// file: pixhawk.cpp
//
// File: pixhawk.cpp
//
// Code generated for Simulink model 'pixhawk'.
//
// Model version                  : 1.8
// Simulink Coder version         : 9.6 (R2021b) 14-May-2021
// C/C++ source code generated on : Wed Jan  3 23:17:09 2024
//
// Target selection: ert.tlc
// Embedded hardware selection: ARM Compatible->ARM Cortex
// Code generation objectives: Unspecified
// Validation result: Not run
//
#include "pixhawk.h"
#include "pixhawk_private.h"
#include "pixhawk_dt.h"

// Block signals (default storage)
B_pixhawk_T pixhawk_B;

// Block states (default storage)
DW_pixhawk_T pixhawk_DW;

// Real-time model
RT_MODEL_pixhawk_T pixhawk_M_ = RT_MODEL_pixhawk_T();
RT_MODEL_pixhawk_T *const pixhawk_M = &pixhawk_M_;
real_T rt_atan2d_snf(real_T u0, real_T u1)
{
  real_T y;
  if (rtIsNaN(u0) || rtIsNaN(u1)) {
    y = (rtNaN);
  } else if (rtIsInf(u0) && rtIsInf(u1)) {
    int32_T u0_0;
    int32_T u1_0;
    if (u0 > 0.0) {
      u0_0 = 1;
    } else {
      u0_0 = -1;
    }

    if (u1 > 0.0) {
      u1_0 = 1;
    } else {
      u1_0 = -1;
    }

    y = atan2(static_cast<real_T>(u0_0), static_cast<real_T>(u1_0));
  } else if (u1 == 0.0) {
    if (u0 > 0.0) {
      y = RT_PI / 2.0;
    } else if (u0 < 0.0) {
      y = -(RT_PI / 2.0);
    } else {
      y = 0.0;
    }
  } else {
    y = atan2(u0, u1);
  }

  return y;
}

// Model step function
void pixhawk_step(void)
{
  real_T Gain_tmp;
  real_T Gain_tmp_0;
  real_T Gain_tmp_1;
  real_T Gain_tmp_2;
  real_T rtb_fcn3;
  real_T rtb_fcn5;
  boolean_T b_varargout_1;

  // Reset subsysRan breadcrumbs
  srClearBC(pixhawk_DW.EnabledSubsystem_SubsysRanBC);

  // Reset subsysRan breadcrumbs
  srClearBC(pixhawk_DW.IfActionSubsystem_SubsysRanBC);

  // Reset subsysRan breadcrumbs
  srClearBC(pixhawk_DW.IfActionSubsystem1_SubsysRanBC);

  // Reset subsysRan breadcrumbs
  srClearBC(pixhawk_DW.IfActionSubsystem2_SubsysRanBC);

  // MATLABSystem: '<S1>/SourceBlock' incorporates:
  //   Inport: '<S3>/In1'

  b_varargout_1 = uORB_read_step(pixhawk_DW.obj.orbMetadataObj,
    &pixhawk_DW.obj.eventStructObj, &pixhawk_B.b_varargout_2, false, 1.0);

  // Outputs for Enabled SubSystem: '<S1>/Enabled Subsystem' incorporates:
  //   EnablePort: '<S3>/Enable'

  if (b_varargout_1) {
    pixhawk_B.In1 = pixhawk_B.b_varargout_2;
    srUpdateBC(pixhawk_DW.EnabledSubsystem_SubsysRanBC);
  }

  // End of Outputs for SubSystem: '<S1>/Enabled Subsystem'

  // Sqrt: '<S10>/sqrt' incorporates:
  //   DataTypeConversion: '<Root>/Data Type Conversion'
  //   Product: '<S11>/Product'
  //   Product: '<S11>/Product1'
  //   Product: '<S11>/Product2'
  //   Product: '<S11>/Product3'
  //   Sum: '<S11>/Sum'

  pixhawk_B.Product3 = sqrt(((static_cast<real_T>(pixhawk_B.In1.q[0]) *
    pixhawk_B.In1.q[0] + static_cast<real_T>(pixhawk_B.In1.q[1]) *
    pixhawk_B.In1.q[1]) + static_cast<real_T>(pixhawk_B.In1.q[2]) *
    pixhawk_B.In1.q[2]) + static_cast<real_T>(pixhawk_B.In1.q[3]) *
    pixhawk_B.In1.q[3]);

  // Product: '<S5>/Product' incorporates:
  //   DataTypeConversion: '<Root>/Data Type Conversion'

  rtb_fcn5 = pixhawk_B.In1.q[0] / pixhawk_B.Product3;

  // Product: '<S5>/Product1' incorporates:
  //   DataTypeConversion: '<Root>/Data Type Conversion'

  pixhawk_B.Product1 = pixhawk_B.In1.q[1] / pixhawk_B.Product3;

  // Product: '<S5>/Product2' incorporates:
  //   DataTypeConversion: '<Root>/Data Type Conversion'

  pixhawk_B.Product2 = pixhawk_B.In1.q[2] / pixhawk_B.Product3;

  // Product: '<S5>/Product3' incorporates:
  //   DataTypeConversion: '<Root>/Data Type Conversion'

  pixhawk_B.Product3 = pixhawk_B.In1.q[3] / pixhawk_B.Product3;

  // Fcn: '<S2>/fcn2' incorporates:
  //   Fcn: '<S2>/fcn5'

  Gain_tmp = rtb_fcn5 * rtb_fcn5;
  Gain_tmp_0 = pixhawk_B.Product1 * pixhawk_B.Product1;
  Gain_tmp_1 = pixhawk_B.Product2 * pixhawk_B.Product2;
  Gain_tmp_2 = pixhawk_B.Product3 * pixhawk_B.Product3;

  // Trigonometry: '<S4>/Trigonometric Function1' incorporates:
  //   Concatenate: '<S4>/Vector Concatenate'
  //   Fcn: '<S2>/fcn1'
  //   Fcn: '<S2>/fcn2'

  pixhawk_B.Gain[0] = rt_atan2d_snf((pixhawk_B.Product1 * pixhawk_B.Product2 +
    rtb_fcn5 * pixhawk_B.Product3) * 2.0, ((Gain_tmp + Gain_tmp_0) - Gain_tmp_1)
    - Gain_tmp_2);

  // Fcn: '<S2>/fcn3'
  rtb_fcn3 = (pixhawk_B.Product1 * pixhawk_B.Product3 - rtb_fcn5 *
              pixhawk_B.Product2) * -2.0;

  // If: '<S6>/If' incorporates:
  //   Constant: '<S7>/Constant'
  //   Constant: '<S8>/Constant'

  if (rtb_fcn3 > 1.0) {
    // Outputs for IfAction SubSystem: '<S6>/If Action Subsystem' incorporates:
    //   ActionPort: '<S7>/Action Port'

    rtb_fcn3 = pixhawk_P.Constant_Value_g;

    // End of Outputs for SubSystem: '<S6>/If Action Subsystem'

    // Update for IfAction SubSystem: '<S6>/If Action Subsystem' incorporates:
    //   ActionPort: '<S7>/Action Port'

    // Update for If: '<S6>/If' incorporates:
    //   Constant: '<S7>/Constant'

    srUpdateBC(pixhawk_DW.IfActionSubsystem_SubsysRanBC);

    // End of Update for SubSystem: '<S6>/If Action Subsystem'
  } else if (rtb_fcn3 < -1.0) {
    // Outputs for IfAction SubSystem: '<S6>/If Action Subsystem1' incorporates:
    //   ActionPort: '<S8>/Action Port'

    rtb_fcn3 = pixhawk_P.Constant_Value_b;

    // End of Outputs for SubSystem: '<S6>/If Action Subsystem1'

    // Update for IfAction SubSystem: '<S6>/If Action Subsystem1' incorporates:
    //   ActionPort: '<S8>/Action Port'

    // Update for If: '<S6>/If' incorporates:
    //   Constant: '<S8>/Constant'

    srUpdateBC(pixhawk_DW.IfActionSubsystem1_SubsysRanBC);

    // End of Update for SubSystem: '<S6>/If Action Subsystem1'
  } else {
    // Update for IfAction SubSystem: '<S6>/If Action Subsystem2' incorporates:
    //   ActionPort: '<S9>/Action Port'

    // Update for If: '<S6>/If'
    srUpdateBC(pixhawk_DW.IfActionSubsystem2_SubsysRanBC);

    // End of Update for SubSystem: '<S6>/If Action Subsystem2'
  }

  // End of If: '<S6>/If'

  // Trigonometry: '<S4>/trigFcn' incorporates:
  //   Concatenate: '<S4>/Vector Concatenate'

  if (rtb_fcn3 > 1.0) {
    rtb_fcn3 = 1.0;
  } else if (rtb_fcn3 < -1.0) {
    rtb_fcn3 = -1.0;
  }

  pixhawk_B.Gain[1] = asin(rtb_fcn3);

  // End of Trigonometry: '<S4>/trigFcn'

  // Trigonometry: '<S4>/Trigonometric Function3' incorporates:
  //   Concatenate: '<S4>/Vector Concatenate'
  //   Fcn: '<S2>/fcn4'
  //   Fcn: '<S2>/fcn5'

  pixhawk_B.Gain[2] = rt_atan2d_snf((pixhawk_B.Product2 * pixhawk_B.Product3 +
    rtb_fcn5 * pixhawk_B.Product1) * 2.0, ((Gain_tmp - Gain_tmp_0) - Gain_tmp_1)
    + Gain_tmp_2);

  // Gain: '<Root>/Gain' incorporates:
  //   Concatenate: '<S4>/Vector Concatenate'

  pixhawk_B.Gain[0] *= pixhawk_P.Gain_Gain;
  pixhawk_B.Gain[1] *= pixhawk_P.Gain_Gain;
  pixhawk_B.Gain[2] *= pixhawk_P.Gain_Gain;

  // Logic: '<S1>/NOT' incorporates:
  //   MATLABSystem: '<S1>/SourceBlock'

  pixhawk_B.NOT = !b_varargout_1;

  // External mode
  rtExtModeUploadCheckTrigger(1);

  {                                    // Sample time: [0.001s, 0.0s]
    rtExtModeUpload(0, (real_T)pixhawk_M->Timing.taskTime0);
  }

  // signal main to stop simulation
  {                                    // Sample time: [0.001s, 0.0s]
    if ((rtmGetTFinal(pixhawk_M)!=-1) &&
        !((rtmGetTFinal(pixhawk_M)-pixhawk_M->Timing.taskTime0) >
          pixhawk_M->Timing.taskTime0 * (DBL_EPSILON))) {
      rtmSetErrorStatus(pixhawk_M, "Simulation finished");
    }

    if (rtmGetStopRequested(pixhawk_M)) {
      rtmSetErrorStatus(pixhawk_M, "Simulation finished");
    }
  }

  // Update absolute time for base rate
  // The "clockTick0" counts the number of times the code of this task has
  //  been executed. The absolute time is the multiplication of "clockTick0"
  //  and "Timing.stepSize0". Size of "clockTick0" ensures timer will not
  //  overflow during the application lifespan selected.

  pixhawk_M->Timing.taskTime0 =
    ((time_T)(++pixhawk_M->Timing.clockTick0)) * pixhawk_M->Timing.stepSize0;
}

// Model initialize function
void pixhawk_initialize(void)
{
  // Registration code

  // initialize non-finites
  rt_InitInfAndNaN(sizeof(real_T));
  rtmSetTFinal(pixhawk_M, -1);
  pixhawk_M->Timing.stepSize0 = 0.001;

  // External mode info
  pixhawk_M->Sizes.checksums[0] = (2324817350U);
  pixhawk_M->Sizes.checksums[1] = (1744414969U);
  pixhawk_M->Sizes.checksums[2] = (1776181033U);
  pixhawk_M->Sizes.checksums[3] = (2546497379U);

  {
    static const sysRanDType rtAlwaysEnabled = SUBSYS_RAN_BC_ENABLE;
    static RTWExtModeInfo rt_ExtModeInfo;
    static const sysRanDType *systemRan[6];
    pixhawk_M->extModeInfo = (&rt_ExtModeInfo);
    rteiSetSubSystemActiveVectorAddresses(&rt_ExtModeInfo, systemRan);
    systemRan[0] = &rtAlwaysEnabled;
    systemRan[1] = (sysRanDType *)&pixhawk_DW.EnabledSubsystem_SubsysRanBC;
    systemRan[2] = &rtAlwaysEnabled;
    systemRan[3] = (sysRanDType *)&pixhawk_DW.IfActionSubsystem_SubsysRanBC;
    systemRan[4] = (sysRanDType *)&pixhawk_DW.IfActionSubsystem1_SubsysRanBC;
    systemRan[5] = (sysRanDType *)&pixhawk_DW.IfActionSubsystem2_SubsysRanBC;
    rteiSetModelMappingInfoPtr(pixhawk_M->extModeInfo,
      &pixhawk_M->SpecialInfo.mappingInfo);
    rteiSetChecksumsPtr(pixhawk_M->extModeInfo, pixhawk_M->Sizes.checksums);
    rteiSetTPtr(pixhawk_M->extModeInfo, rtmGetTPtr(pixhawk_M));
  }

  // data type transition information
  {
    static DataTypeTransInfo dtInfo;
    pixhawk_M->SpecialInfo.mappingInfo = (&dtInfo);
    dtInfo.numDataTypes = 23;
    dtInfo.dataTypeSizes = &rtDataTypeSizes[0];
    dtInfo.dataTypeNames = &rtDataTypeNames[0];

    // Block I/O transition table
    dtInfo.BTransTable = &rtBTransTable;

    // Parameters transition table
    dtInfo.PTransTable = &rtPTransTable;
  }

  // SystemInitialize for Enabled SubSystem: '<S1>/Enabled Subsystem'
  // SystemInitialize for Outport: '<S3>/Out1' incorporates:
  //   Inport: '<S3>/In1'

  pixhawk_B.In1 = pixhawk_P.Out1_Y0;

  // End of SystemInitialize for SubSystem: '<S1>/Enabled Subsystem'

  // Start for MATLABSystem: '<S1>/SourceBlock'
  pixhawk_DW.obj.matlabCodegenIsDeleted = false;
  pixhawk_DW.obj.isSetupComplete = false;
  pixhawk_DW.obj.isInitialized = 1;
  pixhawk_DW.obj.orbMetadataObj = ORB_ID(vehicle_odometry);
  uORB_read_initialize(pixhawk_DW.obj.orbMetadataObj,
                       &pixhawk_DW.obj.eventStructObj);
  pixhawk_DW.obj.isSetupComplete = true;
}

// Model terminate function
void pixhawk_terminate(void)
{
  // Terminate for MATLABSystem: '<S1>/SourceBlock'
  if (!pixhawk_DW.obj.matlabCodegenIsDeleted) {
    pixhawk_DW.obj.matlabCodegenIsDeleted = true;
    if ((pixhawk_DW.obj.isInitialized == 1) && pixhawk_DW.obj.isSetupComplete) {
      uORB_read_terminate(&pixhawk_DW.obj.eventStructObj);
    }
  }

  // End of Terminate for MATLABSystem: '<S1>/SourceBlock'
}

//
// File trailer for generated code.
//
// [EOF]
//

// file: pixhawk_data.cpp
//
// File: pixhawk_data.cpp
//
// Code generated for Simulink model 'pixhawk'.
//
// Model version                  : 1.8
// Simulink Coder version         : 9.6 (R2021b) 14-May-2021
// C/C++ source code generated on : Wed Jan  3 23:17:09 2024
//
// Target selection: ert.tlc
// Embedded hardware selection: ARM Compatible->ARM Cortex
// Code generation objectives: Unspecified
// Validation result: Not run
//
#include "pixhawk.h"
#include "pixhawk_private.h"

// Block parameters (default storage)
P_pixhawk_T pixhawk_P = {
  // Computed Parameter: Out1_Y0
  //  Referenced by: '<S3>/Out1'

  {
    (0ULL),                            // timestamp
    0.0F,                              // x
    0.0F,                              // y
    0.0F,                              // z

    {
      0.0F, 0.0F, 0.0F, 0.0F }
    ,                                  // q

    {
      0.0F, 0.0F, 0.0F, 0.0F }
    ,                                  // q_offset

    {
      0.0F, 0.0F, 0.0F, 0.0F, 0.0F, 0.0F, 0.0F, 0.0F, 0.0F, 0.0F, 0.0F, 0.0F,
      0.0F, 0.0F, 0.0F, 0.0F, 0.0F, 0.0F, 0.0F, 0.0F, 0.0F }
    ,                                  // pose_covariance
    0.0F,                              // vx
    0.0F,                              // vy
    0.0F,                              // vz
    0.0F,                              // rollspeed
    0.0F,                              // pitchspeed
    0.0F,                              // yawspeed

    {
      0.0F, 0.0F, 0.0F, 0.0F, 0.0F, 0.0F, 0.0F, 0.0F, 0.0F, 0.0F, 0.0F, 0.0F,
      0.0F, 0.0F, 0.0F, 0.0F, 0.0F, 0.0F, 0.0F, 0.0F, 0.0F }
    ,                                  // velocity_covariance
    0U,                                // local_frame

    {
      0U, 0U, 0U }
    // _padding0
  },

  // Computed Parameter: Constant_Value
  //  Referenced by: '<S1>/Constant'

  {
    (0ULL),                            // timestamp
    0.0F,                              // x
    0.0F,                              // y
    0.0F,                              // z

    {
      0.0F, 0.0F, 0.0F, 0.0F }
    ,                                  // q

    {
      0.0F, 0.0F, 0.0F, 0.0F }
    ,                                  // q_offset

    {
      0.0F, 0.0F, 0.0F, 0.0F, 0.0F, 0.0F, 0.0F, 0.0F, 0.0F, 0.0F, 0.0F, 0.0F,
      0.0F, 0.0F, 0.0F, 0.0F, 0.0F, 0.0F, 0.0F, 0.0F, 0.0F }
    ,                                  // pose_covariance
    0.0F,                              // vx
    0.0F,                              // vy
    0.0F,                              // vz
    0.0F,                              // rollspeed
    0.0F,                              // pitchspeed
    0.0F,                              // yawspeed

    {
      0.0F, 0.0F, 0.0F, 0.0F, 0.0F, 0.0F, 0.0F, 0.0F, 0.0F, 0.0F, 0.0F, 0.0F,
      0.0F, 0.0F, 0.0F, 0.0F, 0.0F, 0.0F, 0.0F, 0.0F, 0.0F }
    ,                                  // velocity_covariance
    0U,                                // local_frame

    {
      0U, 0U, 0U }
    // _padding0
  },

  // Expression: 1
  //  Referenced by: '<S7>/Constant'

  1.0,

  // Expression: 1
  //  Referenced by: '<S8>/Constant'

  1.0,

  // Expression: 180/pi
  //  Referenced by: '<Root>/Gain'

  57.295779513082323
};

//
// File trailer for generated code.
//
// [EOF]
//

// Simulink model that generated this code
simulink model "pixhawk"  (R2021b)
settings: Solver=FixedStepAuto  StartTime=0.0  StopTime=inf  MaxStep=0.005  RelTol=1e-3  EnableMultiTasking=on
libraries: px4uORBlib x1, sharedtransform x1

== system pixhawk ==
  Bus Selector : BusSelector  OutputSignals=q
  Data Type Conversion : DataTypeConversion  OutDataTypeStr=double
  Demux : Demux  Outputs=3
  Display{,1..3} (4 alike) : Display
  Gain : Gain  Gain=180/pi
  PX4 uORB Read : px4uORBlib/PX4 uORB Read  uORBTopic=vehicle_odometry  selectInstance=vehicle_odometry  SampleTime=0.001  BlockingMode=off  BlockTimeout=1e-3
  Quaternions to Rotation Angles : sharedtransform/Quaternions to Rotation Angles  rotationOrder=ZYX  aMode=aMode
  wires:
  PX4 uORB Read/1 -> Display/1
  PX4 uORB Read/2 -> Bus Selector/1
  Bus Selector/1 -> Data Type Conversion/1  "<q>"
  Data Type Conversion/1 -> Quaternions to Rotation Angles/1
  Quaternions to Rotation Angles/1 -> Gain/1
  Demux/3 -> Display3/1
  Demux/2 -> Display2/1
  Demux/1 -> Display1/1
  Gain/1 -> Demux/1
